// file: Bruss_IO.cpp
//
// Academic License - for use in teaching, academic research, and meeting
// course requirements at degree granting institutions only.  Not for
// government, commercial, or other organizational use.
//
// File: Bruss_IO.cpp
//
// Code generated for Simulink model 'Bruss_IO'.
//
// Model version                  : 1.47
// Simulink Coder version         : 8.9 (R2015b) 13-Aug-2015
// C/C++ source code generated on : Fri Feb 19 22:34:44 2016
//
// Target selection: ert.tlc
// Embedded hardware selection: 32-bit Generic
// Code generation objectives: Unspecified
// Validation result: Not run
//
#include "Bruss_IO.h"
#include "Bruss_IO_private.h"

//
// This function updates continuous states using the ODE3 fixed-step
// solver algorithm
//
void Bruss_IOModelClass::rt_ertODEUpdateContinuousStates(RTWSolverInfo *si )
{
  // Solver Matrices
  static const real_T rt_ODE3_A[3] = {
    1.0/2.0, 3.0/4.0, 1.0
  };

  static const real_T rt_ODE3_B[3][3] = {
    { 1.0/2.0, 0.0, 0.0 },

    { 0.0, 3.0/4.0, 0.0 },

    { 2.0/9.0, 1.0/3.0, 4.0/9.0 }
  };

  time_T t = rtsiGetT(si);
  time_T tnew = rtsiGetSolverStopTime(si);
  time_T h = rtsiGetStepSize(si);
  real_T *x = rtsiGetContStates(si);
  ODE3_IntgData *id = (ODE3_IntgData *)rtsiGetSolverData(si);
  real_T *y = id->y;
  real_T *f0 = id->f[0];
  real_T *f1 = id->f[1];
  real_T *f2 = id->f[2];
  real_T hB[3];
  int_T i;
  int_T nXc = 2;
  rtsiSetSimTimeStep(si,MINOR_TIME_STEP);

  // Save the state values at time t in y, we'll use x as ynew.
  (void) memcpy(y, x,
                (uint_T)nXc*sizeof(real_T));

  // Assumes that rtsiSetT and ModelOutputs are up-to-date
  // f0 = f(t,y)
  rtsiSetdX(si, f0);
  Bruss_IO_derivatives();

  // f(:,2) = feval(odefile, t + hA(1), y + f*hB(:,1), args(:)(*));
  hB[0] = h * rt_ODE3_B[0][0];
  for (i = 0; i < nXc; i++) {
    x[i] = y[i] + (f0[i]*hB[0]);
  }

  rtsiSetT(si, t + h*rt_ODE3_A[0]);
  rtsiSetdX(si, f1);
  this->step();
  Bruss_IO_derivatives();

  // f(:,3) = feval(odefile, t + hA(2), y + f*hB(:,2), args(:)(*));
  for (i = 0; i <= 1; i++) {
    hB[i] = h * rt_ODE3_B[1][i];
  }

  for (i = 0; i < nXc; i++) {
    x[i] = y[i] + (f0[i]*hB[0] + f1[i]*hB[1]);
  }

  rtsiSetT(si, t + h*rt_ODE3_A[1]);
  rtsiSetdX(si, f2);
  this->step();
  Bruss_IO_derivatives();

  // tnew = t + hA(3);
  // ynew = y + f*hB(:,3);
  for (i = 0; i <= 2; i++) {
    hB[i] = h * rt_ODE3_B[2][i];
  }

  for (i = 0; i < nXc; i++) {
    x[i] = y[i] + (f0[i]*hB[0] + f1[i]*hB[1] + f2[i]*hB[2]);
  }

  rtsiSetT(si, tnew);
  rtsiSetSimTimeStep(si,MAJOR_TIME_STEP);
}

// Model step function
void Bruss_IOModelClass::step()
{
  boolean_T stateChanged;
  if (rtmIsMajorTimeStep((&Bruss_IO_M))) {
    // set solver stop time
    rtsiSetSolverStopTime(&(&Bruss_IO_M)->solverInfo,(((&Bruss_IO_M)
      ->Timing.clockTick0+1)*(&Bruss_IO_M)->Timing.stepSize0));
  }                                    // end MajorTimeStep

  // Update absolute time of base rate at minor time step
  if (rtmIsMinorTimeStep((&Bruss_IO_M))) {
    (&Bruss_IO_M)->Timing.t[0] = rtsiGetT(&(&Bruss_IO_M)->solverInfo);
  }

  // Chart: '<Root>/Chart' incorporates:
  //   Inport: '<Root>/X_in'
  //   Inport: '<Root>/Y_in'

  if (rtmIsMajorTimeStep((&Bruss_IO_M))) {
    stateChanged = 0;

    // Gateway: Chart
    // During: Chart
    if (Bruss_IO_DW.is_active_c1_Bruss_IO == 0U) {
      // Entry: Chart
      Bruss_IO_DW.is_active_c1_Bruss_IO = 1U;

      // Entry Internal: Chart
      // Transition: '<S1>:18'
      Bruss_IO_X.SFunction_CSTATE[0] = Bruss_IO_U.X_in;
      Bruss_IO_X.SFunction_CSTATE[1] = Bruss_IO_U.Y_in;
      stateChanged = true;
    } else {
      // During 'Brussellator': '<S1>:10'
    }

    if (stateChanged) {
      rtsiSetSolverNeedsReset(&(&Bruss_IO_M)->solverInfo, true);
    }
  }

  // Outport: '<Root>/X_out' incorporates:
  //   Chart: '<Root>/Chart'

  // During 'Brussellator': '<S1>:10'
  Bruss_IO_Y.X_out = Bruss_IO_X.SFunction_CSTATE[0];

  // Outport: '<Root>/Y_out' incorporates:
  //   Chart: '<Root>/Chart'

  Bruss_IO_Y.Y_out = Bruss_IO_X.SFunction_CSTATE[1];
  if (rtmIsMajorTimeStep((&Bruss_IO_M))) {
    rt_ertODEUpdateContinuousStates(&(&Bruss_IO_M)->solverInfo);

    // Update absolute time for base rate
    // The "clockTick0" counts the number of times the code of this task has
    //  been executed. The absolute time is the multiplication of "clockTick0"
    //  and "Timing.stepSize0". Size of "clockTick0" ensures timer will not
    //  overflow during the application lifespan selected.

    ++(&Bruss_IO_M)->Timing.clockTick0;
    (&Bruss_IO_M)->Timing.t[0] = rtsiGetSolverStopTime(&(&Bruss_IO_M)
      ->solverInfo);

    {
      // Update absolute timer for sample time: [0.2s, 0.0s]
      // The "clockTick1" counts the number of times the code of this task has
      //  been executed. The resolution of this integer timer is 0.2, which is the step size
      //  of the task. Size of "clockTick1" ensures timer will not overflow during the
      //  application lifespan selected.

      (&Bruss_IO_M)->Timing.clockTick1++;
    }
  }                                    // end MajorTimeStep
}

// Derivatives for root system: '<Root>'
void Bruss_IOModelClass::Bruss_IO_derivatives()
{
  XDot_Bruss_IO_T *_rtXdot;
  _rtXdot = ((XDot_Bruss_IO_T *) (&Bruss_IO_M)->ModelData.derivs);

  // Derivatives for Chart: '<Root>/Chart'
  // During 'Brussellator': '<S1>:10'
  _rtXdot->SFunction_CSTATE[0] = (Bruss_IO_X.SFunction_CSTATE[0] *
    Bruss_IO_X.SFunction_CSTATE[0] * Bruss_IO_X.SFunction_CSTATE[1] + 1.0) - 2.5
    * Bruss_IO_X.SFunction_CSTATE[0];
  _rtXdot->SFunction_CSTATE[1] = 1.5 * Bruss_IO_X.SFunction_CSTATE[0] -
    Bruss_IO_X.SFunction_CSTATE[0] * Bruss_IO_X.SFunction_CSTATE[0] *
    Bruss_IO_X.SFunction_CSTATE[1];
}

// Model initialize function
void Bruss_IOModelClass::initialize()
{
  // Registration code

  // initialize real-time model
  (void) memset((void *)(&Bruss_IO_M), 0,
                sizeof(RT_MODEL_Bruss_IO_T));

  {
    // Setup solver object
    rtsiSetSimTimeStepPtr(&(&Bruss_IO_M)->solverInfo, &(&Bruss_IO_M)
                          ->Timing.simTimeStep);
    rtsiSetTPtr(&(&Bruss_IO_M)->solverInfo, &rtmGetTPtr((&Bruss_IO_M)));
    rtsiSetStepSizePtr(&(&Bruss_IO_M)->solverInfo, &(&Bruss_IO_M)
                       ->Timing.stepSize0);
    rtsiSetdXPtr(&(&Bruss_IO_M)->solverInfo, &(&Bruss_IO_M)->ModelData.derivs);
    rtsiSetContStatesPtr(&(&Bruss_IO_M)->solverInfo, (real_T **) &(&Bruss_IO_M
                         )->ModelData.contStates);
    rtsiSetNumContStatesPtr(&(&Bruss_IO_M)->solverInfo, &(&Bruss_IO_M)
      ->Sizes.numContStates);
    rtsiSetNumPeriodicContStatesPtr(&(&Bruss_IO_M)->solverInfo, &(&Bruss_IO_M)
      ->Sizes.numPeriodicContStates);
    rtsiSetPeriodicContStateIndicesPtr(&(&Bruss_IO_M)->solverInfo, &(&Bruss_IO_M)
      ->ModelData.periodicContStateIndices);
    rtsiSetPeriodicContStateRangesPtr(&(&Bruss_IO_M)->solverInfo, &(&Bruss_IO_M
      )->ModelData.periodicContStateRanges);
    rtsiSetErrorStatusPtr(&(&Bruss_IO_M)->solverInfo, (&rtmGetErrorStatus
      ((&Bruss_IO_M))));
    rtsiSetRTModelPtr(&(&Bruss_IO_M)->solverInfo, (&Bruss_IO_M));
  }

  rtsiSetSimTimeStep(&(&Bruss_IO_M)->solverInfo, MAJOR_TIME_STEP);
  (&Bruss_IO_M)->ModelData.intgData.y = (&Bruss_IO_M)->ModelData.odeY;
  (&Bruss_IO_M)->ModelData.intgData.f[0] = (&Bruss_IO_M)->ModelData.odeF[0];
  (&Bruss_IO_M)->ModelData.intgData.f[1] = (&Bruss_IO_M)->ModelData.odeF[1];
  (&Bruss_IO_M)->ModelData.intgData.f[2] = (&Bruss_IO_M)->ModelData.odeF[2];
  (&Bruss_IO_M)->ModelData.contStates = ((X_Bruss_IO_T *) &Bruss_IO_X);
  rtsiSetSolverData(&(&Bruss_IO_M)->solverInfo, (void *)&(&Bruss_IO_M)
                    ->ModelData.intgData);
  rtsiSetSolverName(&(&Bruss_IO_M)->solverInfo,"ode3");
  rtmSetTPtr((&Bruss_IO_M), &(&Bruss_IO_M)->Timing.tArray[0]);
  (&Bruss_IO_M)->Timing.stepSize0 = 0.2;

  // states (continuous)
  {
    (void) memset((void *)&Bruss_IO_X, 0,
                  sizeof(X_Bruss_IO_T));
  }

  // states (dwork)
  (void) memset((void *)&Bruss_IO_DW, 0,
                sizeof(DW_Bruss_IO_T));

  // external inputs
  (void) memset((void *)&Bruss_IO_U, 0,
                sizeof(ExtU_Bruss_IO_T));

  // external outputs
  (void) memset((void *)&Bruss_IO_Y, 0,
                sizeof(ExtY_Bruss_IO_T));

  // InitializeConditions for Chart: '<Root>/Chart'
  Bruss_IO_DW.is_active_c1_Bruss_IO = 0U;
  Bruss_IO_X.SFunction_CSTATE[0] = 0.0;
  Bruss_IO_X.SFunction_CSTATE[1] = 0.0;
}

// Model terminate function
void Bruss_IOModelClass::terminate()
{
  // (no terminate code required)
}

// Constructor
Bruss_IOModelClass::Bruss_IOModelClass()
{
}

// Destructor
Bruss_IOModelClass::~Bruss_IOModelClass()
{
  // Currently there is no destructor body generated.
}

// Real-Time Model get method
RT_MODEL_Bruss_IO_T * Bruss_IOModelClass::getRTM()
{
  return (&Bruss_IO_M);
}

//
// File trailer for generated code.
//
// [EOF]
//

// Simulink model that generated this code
simulink model "Bruss_IO"  (Simulink 8.6)
settings: Solver=ode3  StartTime=0.0  StopTime=10.0  FixedStep=0.2  RelTol=1e-3
libraries: simulink x1

== system Bruss_IO ==
  X_in : Inport
  Y_in : Inport  Port=2
  Chart : Stateflow chart  TreatAsAtomicUnit=on
  Demux : Demux  Commented=on  Outputs=2
  From Workspace : FromWorkspace  Commented=on  VariableName=[t,x,y]  SampleTime=0
  From File : FromFile  Commented=on  FileName=input.mat  SampleTime=0
  Mux : Mux  Inputs=2
  To File : ToFile  Filename=output.mat
  XY Graph : simulink/Sinks/XY Graph  xmin=0  xmax=5  ymin=0  ymax=5  st=-1
  X_out : Outport
  Y_out : Outport  Port=2
  wires:
  Chart/1(x_out) -> X_out/1, Mux/1, XY Graph/1
  From File/1 -> Demux/1
  Mux/1 -> To File/1
  Chart/2(y_out) -> XY Graph/2, Mux/2, Y_out/1
  X_in/1 -> Chart/1(x_in)
  Y_in/1 -> Chart/2(y_in)

== stateflow chart Chart ==
  settings: updateMethod=CONTINUOUS
  state Brussellator
    du:
    x_dot = 1 + x*x*y - 2.5*x;
    y_dot = 1.5*x - x*x*y;
    x_out = x;
    y_out = y;
  note: @annotation-mode=Brussellator;
      | k=2000.0;
      | gamma=0.0;
  (default) -> Brussellator : {x=x_in, y=y_in}
  data: x local double; y local double; x_out output double; y_out output double; x_in input double; y_in input double
  data x settings: updateMethod=SF_CONTINUOUS_TIME_DATA
  data y settings: updateMethod=SF_CONTINUOUS_TIME_DATA
